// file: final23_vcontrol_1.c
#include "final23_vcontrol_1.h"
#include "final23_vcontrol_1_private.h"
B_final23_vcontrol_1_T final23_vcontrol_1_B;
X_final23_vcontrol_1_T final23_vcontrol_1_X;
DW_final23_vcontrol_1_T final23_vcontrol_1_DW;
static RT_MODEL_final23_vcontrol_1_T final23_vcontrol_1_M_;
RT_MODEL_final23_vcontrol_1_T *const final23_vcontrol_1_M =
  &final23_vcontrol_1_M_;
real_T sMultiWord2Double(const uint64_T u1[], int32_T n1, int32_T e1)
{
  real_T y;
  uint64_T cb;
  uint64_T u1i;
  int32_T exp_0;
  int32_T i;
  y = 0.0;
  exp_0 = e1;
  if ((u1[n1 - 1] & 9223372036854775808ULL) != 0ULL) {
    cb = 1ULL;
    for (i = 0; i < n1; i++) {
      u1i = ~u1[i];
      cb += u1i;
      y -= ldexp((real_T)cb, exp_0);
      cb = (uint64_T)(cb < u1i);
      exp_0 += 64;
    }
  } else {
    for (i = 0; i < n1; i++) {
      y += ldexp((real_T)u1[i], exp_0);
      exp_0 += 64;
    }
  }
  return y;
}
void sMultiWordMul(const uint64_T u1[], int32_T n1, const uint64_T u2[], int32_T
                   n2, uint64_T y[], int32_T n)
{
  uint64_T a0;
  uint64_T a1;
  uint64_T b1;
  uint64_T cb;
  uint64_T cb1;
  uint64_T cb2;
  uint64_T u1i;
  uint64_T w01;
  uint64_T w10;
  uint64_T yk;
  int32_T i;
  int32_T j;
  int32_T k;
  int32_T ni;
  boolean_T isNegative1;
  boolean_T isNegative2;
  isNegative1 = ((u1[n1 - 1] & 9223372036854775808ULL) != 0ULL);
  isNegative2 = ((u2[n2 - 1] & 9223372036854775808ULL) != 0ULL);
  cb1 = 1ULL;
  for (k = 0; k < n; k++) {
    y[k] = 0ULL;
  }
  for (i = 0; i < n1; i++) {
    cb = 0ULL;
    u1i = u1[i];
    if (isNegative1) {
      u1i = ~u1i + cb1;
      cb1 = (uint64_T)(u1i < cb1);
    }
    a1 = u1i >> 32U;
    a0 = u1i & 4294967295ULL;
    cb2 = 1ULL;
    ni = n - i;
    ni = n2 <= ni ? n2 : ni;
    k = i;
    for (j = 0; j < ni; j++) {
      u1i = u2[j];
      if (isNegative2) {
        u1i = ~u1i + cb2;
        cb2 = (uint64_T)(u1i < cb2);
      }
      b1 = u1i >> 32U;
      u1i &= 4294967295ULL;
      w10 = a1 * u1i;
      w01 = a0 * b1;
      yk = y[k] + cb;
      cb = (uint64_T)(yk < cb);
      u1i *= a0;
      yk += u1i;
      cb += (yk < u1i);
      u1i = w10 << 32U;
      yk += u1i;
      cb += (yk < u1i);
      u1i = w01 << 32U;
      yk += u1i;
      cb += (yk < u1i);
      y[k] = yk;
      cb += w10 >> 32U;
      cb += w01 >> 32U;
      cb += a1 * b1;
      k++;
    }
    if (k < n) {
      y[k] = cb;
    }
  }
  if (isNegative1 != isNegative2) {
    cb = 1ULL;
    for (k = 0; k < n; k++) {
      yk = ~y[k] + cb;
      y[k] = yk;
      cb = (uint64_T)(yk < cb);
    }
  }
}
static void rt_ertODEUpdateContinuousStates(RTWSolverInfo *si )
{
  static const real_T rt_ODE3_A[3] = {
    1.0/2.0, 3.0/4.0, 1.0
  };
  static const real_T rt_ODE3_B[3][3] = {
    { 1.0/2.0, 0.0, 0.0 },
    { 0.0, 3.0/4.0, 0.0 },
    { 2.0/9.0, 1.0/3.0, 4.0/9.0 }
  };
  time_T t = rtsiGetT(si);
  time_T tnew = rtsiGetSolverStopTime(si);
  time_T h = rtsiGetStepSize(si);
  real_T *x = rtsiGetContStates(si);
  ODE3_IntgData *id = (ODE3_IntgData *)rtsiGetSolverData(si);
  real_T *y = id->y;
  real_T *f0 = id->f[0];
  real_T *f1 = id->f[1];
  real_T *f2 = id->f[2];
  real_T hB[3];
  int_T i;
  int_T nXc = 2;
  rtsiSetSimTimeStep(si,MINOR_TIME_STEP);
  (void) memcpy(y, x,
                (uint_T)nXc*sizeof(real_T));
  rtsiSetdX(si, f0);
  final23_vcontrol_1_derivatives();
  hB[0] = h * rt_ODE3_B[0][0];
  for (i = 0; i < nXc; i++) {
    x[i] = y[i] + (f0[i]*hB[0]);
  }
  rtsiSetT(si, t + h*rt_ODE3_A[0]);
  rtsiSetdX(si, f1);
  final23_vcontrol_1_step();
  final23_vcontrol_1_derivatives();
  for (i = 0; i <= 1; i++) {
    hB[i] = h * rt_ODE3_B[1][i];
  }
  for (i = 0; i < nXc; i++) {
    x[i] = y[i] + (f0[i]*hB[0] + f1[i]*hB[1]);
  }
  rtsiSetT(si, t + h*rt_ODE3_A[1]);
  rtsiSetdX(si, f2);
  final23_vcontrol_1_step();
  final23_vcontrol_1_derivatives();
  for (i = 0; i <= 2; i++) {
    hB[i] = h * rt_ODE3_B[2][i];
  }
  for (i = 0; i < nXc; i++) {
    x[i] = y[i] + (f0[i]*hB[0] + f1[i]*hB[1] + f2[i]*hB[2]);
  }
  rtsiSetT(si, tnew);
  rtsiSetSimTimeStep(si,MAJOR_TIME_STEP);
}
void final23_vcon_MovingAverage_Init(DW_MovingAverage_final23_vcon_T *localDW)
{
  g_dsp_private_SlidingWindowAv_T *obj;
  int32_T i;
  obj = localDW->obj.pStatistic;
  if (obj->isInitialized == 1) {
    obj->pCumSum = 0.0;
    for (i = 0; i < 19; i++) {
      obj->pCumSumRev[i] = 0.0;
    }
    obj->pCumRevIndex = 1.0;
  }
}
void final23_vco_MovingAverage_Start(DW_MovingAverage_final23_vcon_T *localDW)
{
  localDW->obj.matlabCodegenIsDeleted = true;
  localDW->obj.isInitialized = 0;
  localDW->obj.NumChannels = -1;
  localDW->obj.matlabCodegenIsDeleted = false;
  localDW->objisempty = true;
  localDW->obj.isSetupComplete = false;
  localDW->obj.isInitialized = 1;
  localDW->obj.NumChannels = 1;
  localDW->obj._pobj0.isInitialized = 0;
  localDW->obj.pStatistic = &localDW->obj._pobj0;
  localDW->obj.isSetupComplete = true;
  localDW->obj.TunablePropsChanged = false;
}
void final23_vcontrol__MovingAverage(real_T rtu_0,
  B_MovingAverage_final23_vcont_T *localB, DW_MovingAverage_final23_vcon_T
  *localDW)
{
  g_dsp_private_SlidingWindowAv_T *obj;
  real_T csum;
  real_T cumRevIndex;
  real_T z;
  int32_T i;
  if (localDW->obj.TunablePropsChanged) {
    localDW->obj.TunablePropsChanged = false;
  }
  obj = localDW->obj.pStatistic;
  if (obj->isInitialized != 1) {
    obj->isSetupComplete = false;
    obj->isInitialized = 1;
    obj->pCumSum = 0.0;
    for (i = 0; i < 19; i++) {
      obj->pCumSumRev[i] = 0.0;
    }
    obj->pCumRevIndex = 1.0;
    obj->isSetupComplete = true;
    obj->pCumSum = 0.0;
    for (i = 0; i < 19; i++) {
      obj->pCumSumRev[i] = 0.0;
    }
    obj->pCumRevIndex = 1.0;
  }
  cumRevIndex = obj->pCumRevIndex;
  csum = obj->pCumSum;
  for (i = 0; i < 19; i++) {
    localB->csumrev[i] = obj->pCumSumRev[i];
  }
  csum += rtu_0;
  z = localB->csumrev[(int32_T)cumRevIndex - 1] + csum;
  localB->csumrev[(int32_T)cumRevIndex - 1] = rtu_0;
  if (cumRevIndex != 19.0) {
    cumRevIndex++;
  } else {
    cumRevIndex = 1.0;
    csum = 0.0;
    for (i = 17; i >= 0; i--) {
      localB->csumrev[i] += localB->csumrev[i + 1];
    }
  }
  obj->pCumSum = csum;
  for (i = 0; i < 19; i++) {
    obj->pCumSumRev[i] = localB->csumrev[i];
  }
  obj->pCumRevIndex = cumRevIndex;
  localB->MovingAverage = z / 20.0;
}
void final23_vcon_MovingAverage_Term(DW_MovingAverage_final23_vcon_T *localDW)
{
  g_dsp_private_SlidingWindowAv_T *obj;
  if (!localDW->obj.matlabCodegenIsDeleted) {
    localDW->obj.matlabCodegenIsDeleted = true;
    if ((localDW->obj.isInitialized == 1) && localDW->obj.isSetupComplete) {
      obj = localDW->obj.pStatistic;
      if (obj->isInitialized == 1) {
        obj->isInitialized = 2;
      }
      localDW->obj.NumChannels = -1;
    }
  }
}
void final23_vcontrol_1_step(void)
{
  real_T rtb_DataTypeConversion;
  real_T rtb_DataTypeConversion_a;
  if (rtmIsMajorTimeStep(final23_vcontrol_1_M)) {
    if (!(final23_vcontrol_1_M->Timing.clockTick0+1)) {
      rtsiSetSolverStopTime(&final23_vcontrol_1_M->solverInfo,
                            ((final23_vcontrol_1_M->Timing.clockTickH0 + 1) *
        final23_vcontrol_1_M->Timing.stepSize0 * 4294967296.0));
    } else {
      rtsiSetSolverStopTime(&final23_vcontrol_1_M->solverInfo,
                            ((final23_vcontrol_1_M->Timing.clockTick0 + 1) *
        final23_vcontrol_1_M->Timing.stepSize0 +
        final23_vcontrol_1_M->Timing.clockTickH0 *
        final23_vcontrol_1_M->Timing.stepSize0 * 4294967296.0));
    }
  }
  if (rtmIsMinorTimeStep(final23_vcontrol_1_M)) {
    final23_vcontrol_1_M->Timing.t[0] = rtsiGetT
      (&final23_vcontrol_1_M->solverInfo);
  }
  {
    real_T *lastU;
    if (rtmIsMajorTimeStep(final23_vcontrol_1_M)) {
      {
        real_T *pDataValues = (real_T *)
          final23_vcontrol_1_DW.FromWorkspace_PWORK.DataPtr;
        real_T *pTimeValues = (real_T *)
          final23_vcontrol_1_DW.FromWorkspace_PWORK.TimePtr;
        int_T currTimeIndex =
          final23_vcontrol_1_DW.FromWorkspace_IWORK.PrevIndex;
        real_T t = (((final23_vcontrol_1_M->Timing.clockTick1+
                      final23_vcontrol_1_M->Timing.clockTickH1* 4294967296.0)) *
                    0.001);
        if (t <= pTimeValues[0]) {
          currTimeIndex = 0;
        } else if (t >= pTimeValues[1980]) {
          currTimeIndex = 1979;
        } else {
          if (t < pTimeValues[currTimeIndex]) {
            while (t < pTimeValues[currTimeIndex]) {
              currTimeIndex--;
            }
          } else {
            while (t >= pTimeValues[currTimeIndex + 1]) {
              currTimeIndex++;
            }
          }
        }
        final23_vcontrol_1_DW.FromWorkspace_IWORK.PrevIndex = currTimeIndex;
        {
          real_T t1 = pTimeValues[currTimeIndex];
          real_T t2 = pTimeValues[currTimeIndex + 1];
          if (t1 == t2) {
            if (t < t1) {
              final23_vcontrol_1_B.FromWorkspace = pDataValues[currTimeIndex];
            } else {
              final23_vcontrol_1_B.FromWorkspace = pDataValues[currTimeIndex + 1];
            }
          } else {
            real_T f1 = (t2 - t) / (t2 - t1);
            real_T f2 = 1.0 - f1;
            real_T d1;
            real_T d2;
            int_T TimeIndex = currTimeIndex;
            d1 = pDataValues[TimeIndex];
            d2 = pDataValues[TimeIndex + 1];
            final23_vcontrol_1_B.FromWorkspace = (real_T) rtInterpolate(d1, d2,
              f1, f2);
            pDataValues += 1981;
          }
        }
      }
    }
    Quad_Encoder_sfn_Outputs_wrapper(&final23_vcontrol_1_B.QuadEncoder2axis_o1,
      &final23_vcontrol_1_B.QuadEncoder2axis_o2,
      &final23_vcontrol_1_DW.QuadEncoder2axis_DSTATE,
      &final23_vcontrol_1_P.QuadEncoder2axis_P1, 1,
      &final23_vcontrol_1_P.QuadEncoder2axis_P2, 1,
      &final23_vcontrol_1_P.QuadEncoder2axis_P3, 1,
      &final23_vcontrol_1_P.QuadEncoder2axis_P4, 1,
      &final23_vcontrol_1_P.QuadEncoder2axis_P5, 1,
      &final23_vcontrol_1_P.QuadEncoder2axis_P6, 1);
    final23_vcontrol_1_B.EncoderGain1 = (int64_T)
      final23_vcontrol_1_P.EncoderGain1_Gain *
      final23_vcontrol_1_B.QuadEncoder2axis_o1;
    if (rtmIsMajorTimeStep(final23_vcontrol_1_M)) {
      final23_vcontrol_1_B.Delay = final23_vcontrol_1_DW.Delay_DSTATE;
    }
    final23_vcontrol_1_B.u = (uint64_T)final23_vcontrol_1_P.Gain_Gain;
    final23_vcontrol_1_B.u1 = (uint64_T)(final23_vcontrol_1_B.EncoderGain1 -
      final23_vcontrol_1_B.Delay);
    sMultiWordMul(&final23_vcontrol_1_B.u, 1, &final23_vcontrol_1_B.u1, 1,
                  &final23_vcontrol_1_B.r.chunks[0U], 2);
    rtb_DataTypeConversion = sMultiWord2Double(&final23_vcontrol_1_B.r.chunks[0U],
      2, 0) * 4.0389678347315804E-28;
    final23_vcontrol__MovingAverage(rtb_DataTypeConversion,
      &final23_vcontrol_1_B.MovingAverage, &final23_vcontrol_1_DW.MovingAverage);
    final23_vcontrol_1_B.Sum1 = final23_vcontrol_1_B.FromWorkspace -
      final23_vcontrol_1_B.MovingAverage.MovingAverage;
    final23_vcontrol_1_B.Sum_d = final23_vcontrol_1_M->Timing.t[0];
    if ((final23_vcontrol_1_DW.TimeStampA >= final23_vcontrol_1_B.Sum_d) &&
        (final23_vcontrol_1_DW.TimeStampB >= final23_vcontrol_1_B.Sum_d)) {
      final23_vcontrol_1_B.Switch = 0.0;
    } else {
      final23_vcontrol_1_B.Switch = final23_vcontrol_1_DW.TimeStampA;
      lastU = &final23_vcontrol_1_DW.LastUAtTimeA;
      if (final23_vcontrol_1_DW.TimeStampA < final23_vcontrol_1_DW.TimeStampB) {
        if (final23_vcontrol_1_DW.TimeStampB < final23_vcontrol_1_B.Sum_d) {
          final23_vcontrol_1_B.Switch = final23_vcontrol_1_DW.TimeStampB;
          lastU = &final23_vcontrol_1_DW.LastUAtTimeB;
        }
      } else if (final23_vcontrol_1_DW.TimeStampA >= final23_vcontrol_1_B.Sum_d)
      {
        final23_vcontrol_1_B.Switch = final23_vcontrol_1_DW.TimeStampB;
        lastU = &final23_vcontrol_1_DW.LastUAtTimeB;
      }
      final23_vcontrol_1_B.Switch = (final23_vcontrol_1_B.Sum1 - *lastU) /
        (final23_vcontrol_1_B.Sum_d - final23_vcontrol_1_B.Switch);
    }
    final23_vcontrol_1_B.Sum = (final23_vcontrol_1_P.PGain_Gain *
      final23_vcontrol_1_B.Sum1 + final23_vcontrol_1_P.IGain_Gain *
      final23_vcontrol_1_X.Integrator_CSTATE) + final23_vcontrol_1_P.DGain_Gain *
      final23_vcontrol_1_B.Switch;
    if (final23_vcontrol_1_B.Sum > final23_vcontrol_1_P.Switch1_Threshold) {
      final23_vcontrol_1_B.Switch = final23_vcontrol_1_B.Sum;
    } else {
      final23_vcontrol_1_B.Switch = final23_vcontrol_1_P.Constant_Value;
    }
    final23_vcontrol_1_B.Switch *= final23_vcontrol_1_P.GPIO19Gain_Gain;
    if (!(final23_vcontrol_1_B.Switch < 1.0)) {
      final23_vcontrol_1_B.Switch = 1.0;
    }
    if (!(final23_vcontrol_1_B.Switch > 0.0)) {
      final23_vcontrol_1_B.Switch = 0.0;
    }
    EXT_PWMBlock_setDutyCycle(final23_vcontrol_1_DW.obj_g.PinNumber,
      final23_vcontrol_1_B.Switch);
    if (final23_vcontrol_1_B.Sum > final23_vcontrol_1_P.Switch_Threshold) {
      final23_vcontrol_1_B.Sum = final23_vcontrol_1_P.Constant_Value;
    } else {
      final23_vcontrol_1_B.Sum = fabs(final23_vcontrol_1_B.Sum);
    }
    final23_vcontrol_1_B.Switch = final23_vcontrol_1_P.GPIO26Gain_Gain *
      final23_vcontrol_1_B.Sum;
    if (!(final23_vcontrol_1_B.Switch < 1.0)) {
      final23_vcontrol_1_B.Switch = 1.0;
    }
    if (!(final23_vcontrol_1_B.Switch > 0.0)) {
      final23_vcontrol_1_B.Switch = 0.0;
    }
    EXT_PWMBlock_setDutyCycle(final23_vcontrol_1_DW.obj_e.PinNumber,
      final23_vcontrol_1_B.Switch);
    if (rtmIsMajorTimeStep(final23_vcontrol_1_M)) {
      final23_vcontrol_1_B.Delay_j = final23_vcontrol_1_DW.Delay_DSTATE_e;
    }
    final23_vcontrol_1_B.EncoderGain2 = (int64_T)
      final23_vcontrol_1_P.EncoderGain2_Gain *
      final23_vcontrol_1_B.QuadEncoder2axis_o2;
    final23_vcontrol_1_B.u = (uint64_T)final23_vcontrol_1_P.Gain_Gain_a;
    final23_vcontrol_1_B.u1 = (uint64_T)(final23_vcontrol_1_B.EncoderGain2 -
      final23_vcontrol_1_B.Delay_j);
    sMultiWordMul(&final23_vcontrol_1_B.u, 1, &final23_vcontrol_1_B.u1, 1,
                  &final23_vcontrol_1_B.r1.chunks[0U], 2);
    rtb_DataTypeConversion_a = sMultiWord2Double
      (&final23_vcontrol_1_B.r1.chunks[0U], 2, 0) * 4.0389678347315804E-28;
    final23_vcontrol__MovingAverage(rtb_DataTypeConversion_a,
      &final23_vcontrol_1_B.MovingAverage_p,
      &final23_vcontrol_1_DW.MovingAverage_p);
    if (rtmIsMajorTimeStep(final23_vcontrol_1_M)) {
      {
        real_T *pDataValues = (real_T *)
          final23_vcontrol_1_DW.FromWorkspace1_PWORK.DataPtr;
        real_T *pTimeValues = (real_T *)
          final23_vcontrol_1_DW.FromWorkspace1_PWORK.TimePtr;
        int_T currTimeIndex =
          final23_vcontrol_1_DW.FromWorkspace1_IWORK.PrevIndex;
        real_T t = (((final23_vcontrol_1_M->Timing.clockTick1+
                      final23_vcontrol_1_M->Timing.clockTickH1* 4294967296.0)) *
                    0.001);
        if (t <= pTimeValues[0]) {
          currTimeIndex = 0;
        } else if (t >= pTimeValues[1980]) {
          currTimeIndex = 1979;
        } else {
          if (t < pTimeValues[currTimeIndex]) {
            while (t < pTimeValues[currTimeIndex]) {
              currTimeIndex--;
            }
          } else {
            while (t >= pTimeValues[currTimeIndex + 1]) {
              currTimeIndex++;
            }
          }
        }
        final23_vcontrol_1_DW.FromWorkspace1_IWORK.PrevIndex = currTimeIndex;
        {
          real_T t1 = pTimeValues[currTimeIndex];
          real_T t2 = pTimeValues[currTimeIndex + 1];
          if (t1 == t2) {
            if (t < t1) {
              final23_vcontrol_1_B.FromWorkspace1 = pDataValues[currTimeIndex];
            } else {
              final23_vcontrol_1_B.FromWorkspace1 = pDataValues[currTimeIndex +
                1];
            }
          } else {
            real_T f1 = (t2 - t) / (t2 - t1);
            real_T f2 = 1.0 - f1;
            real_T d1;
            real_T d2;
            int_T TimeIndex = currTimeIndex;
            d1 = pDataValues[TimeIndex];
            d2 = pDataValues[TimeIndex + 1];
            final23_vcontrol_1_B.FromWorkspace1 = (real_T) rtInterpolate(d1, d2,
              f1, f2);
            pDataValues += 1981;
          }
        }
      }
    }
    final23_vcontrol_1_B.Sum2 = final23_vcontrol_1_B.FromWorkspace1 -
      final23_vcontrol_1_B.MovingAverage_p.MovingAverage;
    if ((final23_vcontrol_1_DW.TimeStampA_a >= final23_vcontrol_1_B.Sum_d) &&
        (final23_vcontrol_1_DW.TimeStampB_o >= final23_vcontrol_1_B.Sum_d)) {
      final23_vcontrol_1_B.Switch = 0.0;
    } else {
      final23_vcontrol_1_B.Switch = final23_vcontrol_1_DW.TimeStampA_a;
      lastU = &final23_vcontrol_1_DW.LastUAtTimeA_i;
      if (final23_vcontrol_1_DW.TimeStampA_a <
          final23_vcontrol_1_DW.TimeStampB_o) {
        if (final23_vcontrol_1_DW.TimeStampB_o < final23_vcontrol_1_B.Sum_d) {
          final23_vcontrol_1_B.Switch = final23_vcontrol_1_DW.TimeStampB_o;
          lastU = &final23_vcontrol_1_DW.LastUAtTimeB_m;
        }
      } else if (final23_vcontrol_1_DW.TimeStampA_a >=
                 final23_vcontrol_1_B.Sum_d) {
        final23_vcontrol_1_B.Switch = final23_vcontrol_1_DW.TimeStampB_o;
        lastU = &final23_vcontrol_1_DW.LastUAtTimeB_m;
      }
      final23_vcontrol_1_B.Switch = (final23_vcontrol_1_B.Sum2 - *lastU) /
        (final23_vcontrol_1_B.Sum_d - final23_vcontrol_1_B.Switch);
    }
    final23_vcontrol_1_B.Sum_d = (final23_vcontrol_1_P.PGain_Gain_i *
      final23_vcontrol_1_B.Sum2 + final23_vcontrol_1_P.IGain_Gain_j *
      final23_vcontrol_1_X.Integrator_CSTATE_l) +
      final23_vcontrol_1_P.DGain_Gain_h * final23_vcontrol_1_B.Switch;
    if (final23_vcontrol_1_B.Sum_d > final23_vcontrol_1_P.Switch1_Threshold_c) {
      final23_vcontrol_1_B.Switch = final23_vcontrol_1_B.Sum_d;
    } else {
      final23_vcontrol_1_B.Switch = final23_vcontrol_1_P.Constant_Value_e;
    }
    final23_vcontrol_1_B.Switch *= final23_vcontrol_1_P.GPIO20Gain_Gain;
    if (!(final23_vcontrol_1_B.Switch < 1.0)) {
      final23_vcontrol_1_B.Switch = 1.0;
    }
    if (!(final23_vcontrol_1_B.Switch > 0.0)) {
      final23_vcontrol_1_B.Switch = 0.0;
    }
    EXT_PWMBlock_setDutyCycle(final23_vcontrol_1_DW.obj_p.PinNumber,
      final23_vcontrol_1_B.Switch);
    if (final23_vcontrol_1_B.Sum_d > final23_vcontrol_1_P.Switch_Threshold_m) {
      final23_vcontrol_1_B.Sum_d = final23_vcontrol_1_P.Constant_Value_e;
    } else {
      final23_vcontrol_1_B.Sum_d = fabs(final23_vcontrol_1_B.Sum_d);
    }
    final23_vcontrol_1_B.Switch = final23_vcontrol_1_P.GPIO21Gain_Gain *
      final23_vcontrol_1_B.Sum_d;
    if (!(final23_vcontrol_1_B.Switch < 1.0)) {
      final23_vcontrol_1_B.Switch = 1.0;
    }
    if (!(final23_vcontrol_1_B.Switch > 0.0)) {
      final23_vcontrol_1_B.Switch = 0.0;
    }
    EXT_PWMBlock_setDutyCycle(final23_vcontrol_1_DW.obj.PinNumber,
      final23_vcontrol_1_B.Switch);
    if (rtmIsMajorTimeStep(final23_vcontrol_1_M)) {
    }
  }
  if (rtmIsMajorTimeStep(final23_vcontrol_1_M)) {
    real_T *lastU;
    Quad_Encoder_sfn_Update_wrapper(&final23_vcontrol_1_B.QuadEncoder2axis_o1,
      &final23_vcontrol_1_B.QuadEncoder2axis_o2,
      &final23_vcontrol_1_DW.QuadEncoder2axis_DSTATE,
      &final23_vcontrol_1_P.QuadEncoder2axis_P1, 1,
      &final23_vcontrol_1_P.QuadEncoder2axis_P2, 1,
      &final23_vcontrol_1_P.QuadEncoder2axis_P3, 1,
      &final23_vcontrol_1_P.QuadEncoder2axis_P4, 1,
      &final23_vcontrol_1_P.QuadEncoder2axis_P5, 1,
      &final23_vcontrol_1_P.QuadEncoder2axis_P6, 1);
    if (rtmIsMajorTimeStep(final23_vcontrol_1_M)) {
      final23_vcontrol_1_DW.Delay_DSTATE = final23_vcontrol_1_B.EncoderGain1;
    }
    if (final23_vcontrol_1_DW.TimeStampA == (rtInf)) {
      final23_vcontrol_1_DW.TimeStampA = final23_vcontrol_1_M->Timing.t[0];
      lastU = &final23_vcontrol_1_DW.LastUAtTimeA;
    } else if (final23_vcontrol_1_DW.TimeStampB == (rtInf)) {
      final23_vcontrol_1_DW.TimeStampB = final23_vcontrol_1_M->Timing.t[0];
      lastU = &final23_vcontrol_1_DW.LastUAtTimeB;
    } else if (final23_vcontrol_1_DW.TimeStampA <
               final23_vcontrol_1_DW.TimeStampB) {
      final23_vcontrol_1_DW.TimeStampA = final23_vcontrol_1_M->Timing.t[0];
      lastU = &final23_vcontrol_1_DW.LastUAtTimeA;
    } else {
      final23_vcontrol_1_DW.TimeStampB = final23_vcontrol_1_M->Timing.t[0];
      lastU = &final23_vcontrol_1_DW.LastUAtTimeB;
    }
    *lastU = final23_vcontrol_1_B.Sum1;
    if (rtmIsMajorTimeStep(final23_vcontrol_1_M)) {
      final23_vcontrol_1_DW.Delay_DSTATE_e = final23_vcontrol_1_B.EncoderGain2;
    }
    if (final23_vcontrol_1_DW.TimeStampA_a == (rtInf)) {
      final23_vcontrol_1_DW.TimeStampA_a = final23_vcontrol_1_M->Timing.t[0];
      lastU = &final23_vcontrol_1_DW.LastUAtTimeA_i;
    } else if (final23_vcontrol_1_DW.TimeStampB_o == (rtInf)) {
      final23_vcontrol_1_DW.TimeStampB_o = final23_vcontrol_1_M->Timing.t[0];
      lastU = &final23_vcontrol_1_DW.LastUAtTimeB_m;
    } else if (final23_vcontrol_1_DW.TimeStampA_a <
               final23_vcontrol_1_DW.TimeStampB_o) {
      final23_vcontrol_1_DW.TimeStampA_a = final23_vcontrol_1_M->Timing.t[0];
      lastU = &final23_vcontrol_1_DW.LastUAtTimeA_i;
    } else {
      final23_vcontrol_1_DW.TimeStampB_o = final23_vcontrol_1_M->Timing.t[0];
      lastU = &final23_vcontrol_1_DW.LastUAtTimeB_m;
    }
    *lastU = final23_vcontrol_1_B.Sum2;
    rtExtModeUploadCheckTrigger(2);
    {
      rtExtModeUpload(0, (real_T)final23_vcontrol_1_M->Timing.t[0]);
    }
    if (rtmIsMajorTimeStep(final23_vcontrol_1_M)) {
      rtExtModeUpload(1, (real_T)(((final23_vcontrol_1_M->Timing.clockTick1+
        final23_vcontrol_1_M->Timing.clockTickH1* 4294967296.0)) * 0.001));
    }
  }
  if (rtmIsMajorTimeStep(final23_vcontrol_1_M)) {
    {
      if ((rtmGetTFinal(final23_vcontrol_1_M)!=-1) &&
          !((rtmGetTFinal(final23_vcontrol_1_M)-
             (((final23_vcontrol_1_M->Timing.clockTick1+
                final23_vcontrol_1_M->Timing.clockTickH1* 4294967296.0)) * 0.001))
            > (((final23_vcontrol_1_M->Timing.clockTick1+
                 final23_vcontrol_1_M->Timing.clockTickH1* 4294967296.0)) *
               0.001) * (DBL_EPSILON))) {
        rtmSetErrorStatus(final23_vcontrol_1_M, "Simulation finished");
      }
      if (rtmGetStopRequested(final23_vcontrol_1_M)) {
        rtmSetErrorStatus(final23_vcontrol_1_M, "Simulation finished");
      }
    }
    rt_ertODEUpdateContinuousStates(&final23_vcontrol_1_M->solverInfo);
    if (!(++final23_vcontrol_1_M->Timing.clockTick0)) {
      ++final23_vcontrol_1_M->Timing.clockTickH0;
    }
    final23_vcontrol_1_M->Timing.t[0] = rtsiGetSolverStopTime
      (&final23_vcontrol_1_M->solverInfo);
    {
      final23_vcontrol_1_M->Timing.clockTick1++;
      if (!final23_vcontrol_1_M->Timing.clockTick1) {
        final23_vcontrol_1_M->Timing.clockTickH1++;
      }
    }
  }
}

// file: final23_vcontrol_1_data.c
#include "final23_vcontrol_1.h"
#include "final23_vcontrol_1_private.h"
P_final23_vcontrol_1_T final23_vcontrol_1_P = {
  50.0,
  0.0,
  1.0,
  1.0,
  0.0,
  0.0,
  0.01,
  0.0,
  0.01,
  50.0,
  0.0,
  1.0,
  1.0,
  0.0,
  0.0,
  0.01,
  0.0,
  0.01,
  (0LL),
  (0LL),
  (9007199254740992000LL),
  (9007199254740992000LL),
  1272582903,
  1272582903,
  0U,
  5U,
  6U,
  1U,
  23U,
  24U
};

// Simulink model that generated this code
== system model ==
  PWM#1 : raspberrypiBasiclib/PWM  Frequency=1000  <- 1: GPIO19Gain
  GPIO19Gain : Gain  Gain=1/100  <- 1: Switch1
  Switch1 : Switch  Criteria=u2 > Threshold  <- 1: Sum, 2: Sum, 3: Constant
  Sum : Sum  Inputs=+++  <- 1: PGain, 2: IGain, 3: DGain
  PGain : Gain  Gain=50  <- 1: Sum1
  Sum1 : Sum  Inputs=+-  <- 1: FromWorkspace, 2: MovingAverage
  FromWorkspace : FromWorkspace
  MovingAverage : dspstat3/Moving Average  <- 1: DataTypeConversion
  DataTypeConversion : DataTypeConversion  <- 1: Gain
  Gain : Gain  Gain=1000  <- 1: Sum#1
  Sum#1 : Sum  Inputs=+-  <- 1: EncoderGain1, 2: Delay
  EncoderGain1 : Gain  Gain=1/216  <- 1: QuadEncoder2axis
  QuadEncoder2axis : S-Function  FunctionName=Quad_Encoder_sfn
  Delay : Delay  DelayLength=1  <- 1: EncoderGain1
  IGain : Gain  <- 1: Integrator
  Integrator : Integrator  <- 1: Sum1
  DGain : Gain  <- 1: Derivative#1
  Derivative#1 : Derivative  <- 1: Sum1
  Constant : Constant  Value=0
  PWM#2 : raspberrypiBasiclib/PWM  Frequency=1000  <- 1: GPIO26Gain
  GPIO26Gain : Gain  Gain=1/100  <- 1: Switch
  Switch : Switch  Criteria=u2 > Threshold  <- 1: Constant, 2: Sum, 3: Abs#1
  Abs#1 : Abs  <- 1: Sum
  PWM#3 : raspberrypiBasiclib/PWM  Frequency=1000  <- 1: GPIO20Gain
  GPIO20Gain : Gain  Gain=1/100  <- 1: Switch#1
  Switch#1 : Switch  Criteria=u2 > Threshold  <- 1: Sum#2, 2: Sum#2, 3: Constant#1
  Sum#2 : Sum  Inputs=+++  <- 1: Gain#1, 2: Gain#2, 3: Gain#3
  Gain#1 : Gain  Gain=50  <- 1: Sum2
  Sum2 : Sum  Inputs=-+  <- 1: MovingAverage#1, 2: FromWorkspace1
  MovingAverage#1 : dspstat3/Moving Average  <- 1: DataTypeConversion#1
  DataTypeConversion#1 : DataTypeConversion  <- 1: Gain#4
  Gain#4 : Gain  Gain=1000  <- 1: Sum#3
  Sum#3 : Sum  Inputs=+-  <- 1: EncoderGain2, 2: Delay#1
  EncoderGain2 : Gain  Gain=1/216  <- 1: QuadEncoder2axis/2
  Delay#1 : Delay  DelayLength=1  <- 1: EncoderGain2
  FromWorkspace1 : FromWorkspace
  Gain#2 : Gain  <- 1: Integrator#1
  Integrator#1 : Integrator  <- 1: Sum2
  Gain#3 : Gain  <- 1: Derivative#2
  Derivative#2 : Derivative  <- 1: Sum2
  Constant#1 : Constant  Value=0
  PWM#4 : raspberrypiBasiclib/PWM  Frequency=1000  <- 1: GPIO21Gain
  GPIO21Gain : Gain  Gain=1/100  <- 1: Switch#2
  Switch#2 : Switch  Criteria=u2 > Threshold  <- 1: Constant#1, 2: Sum#2, 3: Abs#2
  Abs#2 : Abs  <- 1: Sum#2
